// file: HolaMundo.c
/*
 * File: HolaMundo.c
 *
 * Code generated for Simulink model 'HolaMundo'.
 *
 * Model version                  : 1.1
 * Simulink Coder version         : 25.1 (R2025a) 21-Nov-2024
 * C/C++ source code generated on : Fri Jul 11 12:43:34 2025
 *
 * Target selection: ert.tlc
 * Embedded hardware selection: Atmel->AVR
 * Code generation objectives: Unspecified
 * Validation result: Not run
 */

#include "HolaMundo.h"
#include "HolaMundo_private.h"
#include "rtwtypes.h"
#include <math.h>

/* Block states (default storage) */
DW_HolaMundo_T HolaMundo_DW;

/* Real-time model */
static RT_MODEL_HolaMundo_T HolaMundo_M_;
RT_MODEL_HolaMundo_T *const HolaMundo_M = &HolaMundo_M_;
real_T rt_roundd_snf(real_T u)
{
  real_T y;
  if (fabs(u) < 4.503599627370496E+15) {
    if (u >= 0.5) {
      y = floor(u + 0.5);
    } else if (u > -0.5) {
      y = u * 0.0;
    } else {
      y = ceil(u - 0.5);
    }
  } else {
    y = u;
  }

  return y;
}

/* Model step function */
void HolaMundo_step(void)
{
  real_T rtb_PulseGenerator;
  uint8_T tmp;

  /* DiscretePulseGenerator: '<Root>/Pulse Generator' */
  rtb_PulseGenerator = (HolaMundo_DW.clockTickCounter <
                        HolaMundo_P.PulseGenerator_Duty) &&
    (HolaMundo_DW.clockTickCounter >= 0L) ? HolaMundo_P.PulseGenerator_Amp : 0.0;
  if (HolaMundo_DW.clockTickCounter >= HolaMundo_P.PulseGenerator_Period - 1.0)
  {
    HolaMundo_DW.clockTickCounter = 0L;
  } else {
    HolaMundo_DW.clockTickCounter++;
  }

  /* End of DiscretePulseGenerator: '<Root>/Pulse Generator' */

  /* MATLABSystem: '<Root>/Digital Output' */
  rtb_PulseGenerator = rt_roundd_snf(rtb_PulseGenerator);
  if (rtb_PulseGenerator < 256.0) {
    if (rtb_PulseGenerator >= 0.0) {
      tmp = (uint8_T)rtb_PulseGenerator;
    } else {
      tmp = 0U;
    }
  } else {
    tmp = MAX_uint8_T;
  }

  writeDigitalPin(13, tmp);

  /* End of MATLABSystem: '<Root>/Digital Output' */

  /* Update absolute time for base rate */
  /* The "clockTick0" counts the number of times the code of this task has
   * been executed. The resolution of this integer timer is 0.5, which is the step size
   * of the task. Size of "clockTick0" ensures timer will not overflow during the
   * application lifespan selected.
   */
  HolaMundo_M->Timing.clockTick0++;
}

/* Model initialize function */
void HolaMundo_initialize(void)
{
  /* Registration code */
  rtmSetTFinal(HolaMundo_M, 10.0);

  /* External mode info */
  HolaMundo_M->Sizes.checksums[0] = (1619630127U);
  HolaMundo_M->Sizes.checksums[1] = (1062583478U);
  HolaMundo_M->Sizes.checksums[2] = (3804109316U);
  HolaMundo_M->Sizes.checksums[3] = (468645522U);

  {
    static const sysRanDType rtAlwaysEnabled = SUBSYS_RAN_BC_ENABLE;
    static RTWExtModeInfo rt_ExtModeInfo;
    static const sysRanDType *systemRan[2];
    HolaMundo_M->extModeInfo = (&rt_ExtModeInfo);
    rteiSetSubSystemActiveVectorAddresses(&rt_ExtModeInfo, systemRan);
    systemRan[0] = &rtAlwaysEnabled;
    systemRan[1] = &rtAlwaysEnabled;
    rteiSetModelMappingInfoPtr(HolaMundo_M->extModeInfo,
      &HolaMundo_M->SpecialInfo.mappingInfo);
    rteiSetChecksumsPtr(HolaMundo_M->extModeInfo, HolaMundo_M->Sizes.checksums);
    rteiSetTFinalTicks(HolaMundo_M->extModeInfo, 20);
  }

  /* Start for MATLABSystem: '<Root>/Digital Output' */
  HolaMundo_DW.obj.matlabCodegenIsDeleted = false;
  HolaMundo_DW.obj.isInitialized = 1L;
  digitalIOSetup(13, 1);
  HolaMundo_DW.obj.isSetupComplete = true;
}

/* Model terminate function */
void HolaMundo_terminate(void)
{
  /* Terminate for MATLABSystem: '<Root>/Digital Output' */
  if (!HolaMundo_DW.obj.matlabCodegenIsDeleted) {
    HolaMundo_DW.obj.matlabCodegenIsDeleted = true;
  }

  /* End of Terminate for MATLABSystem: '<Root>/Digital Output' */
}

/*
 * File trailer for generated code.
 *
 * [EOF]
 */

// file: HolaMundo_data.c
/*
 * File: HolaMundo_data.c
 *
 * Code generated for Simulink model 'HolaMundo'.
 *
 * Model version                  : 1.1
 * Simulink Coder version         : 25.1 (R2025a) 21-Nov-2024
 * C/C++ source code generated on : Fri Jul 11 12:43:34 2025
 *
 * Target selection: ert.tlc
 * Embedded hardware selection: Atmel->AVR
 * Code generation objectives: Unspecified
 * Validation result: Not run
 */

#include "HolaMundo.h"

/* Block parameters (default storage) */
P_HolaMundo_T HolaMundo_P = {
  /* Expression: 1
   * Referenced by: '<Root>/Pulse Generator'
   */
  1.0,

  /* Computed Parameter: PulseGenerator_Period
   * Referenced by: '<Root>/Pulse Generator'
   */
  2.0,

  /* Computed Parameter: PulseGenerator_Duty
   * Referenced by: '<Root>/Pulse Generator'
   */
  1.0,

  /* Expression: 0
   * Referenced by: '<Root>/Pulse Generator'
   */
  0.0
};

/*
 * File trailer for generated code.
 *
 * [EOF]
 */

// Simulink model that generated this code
simulink model "HolaMundo"  (R2025a)
settings: Solver=FixedStepAuto  StartTime=0.0  StopTime=10.0  RelTol=1e-3  EnableMultiTasking=on
libraries: arduinolib x1

== system HolaMundo ==
  Digital Output : arduinolib/Digital Output  pinNumber=13  Direction=output  blockPlatform=arduino
  Pulse Generator : DiscretePulseGenerator  PulseType=Time based  Period=1  PulseWidth=50
  wires:
  Pulse Generator/1 -> Digital Output/1
